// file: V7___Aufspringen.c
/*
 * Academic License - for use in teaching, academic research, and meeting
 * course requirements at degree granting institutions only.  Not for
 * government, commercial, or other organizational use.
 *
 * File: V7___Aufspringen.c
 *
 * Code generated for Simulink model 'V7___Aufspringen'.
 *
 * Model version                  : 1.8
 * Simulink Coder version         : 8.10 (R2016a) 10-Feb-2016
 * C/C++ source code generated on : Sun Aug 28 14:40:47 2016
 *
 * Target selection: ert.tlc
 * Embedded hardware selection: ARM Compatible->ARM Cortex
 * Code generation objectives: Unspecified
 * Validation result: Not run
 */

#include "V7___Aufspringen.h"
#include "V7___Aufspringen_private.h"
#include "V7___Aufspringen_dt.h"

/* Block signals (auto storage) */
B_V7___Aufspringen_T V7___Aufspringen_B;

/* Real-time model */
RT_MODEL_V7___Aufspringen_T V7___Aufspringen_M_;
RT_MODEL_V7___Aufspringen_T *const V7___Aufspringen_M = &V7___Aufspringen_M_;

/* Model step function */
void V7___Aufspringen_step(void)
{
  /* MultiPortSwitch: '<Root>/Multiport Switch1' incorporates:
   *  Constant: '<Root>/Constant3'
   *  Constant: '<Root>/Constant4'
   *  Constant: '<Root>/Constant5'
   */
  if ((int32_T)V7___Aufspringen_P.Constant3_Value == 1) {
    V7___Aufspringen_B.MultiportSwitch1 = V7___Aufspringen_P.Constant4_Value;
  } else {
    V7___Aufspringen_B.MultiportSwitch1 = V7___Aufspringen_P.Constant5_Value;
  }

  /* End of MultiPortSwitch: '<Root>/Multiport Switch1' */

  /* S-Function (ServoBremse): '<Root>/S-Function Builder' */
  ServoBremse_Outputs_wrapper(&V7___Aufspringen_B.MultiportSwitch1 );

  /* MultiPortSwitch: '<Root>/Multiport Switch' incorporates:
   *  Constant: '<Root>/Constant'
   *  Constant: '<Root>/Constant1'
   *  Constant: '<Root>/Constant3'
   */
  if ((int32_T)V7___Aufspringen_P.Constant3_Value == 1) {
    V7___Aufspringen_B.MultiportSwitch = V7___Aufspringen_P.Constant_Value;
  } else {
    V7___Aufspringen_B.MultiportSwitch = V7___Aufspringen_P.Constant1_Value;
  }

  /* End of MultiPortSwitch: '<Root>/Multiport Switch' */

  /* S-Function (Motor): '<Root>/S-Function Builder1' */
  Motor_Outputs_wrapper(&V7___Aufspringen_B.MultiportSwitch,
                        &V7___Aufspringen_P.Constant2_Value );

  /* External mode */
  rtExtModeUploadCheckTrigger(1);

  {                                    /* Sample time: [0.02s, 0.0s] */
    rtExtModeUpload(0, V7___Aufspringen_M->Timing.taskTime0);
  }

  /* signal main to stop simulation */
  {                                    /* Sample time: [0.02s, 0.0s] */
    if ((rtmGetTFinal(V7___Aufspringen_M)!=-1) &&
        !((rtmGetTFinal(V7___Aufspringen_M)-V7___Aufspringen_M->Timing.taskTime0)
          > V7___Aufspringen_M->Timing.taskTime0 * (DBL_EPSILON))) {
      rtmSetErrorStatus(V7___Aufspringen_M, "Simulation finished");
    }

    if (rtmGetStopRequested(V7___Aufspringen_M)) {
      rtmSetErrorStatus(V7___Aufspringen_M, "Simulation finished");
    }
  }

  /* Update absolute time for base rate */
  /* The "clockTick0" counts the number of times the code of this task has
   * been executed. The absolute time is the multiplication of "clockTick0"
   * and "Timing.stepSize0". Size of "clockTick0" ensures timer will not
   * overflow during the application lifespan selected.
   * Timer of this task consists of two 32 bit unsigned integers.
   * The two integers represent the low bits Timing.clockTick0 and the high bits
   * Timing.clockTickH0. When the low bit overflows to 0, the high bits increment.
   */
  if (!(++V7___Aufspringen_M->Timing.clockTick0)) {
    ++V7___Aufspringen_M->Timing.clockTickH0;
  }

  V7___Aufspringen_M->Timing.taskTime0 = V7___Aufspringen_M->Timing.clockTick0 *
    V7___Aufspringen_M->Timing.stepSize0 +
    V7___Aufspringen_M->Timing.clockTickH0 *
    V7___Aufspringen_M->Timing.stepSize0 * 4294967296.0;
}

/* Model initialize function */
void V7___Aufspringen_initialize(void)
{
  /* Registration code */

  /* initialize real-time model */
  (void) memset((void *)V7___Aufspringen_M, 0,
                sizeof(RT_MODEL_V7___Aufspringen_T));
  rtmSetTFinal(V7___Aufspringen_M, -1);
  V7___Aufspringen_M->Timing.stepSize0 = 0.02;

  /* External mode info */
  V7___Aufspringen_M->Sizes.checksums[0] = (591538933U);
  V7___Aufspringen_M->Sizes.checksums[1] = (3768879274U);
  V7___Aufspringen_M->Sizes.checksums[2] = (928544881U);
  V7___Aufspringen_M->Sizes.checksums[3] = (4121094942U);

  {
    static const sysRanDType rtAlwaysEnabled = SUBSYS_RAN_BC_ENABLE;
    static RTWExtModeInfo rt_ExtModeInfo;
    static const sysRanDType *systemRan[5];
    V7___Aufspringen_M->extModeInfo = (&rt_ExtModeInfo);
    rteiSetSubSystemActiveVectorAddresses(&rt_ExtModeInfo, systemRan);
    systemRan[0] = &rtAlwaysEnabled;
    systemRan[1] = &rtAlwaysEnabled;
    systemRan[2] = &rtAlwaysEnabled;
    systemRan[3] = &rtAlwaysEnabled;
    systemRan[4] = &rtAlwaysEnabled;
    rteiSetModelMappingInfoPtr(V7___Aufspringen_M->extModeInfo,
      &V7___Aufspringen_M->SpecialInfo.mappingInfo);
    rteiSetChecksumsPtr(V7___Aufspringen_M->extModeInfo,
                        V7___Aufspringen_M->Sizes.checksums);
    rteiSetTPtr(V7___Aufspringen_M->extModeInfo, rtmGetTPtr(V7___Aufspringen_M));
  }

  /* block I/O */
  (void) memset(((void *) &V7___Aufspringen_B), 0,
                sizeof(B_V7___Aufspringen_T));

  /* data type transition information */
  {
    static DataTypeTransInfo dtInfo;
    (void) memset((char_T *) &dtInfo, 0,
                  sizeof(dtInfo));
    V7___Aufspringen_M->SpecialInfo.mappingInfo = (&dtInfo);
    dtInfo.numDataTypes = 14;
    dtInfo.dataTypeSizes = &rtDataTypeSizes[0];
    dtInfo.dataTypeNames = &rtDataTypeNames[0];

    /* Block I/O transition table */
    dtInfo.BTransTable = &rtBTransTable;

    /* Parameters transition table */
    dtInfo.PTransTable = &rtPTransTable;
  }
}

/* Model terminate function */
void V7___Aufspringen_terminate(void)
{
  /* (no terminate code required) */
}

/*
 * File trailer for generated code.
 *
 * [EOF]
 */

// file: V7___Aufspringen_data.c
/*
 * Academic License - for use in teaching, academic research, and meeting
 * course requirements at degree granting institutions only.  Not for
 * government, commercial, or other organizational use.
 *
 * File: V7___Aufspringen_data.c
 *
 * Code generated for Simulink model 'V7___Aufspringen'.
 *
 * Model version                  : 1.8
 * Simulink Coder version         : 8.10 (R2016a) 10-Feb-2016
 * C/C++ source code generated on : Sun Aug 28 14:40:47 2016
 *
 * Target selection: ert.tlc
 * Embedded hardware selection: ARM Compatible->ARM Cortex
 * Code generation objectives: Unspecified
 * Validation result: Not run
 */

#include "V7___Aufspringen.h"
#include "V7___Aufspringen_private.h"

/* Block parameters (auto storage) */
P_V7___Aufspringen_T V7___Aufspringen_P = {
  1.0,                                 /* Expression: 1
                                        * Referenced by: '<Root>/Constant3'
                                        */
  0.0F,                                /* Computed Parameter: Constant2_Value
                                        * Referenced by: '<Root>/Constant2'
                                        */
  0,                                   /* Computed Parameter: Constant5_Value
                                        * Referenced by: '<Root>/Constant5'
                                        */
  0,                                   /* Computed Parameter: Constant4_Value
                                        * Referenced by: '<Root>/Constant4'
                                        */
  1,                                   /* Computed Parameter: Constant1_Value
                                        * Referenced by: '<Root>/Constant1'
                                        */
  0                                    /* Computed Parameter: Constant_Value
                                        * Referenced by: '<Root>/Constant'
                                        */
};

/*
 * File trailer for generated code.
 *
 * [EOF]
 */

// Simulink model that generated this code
simulink model "V7___Aufspringen"  (R2016a)
settings: Solver=FixedStepDiscrete  StartTime=0.0  StopTime=inf  FixedStep=0.02  RelTol=1e-3

== system V7___Aufspringen ==
  Constant{,2,4..5} (4 alike) : Constant  Value=0  OutDataTypeStr=Inherit: Inherit via back propagation
  Constant1 : Constant  OutDataTypeStr=Inherit: Inherit via back propagation
  Constant3 : Constant
  Multiport Switch : MultiPortSwitch  Inputs=2
  Multiport Switch1 : MultiPortSwitch  Inputs=2
  S-Function Builder : S-Function  InitFcn=try, set_param(gcb,'FunctionName','ServoBremse'), end  FunctionName=ServoBremse  SFunctionModules=ServoBremse_wrapper  SFunctionDeploymentMode=off  EnableBusSupport=off  mask(S-Function Builder){}
      mask help: Simulink:masks:SFunctionBuilder_MD
      mask init:
      | val = [[.9  0.75 0.75 1 1 .9 .9 1]',[1 1 0.75 0.75 .9 .9 1 .9]'];try , sys = get_param(gcb,'SfunBuilderFcnName');if isempty(sys), sys = get_param(gcb,'FunctionName'); end,catch, sys = get_param(gcb,'FunctionName'); end
  S-Function Builder1 : S-Function  InitFcn=try, set_param(gcb,'FunctionName','Motor'), end  FunctionName=Motor  SFunctionModules=Motor_wrapper  SFunctionDeploymentMode=off  EnableBusSupport=off  mask(S-Function Builder){}
      mask help: Simulink:masks:SFunctionBuilder_MD
      mask init: same as V7___Aufspringen/S-Function Builder
  wires:
  Multiport Switch1/1 -> S-Function Builder/1
  Constant/1 -> Multiport Switch/2
  Constant1/1 -> Multiport Switch/3
  Multiport Switch/1 -> S-Function Builder1/1
  Constant4/1 -> Multiport Switch1/2
  Constant5/1 -> Multiport Switch1/3
  Constant3/1 -> Multiport Switch1/1, Multiport Switch/1
  Constant2/1 -> S-Function Builder1/2
